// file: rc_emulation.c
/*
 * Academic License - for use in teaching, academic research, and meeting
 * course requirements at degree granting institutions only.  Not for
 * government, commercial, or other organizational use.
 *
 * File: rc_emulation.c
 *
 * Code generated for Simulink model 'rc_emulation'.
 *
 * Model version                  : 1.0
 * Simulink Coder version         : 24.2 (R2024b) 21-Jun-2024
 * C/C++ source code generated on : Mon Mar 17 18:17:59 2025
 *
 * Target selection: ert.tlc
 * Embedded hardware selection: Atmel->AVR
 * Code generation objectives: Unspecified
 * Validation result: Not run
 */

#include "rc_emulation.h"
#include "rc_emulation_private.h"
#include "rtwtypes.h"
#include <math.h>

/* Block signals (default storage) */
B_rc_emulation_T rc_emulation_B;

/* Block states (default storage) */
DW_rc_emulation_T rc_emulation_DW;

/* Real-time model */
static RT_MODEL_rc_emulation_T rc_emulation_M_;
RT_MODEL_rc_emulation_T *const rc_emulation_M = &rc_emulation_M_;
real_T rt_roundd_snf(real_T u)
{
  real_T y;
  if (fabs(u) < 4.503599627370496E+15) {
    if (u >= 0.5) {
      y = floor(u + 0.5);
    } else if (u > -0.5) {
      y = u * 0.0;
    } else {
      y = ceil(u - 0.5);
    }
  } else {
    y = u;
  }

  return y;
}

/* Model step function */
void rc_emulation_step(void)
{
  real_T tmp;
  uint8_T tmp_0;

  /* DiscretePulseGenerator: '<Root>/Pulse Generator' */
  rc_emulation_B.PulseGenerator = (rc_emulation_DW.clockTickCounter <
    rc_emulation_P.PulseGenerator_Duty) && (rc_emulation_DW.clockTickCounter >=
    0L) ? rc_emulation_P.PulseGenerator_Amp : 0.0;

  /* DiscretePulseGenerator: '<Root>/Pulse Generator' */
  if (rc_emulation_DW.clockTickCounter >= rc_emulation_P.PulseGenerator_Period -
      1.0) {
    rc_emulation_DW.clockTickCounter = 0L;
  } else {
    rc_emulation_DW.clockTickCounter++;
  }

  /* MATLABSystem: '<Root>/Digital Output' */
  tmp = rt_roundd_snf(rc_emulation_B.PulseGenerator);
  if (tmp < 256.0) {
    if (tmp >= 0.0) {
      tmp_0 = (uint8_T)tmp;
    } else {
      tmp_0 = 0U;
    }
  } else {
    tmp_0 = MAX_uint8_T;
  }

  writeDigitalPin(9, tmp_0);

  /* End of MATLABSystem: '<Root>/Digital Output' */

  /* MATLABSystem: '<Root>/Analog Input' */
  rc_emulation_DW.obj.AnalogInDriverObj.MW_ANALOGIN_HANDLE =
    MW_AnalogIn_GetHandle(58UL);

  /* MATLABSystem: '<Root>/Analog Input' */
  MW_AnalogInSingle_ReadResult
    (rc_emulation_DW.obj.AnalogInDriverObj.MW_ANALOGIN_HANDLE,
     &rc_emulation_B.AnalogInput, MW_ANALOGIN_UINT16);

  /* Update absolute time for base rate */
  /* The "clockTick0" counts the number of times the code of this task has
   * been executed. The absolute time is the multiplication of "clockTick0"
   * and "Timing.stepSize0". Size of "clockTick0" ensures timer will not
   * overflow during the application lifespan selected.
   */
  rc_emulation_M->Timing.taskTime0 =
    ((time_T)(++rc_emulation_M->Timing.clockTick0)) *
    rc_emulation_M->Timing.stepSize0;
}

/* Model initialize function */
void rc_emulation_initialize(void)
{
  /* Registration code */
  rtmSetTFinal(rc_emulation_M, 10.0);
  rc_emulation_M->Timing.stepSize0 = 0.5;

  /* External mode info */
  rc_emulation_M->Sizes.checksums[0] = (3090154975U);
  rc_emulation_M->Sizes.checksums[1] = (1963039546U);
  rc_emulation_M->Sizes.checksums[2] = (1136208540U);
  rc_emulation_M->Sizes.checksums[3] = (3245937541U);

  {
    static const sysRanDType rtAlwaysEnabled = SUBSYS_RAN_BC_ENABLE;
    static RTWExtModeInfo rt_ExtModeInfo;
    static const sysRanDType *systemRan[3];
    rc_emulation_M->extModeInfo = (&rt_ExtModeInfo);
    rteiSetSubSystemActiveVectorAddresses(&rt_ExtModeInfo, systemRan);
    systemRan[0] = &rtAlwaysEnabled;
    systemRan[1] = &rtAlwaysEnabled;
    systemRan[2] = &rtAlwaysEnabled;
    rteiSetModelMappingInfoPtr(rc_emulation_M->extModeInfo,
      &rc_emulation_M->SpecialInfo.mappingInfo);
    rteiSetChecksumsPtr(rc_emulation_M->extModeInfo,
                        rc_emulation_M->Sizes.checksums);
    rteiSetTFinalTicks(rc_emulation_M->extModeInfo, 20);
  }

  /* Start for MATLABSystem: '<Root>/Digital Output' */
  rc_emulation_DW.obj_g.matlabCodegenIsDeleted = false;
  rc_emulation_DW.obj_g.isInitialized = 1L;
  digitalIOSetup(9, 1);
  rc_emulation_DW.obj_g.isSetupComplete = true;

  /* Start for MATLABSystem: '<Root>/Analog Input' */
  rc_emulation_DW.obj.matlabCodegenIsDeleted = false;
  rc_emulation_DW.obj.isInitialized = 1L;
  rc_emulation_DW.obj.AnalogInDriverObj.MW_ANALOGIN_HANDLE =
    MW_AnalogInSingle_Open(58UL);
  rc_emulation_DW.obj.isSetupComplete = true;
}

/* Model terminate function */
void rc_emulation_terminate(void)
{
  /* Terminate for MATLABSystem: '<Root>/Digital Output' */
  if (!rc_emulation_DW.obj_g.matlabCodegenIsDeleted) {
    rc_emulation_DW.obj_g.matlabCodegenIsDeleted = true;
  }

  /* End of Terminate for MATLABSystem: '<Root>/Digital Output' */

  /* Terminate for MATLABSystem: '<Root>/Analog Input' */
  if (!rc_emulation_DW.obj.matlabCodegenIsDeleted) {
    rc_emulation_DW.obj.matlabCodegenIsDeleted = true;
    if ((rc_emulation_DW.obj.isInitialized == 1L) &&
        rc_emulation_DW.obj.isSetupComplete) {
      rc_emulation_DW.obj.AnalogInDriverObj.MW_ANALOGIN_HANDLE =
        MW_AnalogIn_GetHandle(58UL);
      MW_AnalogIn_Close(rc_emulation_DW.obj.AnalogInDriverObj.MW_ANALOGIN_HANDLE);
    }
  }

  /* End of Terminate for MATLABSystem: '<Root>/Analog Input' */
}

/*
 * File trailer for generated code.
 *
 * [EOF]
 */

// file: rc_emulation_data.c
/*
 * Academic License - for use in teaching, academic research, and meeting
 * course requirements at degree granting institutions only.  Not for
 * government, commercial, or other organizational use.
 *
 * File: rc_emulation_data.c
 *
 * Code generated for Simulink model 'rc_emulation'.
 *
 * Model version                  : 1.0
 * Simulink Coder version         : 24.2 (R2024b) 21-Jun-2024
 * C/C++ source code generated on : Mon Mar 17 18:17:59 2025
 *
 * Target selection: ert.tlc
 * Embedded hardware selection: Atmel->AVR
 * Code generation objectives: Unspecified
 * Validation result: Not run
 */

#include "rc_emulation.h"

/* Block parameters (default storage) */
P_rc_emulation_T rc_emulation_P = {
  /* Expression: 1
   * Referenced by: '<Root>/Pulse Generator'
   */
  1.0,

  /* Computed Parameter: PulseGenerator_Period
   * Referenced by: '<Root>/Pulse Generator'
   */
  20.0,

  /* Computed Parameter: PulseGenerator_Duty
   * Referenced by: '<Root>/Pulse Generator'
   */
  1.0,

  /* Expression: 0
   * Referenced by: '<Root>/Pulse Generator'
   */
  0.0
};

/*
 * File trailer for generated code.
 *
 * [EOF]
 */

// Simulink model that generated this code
simulink model "rc_emulation"  (R2024b)
settings: Solver=FixedStepAuto  StartTime=0.0  StopTime=10.0  RelTol=1e-3  EnableMultiTasking=on
libraries: arduinolib x2

== system rc_emulation ==
  Analog Input : arduinolib/Analog Input  pinNumber=4  ReadResultsOnly=off  ConversionTriggerSource=Software  ExternalTriggerType=uint32( 0 )  OutputDataType=uint16  EnableConversionCompleteNotify=off  EnableOuputStatus=off  SampleTime=-1  blockPlatform=arduino
  Digital Output : arduinolib/Digital Output  pinNumber=9  Direction=output  blockPlatform=arduino
  Pulse Generator : DiscretePulseGenerator  PulseType=Time based  Period=10  PulseWidth=5
  Scope : Scope  NumInputPorts=2
  wires:
  Pulse Generator/1 -> Scope/1, Digital Output/1
  Analog Input/1 -> Scope/2
